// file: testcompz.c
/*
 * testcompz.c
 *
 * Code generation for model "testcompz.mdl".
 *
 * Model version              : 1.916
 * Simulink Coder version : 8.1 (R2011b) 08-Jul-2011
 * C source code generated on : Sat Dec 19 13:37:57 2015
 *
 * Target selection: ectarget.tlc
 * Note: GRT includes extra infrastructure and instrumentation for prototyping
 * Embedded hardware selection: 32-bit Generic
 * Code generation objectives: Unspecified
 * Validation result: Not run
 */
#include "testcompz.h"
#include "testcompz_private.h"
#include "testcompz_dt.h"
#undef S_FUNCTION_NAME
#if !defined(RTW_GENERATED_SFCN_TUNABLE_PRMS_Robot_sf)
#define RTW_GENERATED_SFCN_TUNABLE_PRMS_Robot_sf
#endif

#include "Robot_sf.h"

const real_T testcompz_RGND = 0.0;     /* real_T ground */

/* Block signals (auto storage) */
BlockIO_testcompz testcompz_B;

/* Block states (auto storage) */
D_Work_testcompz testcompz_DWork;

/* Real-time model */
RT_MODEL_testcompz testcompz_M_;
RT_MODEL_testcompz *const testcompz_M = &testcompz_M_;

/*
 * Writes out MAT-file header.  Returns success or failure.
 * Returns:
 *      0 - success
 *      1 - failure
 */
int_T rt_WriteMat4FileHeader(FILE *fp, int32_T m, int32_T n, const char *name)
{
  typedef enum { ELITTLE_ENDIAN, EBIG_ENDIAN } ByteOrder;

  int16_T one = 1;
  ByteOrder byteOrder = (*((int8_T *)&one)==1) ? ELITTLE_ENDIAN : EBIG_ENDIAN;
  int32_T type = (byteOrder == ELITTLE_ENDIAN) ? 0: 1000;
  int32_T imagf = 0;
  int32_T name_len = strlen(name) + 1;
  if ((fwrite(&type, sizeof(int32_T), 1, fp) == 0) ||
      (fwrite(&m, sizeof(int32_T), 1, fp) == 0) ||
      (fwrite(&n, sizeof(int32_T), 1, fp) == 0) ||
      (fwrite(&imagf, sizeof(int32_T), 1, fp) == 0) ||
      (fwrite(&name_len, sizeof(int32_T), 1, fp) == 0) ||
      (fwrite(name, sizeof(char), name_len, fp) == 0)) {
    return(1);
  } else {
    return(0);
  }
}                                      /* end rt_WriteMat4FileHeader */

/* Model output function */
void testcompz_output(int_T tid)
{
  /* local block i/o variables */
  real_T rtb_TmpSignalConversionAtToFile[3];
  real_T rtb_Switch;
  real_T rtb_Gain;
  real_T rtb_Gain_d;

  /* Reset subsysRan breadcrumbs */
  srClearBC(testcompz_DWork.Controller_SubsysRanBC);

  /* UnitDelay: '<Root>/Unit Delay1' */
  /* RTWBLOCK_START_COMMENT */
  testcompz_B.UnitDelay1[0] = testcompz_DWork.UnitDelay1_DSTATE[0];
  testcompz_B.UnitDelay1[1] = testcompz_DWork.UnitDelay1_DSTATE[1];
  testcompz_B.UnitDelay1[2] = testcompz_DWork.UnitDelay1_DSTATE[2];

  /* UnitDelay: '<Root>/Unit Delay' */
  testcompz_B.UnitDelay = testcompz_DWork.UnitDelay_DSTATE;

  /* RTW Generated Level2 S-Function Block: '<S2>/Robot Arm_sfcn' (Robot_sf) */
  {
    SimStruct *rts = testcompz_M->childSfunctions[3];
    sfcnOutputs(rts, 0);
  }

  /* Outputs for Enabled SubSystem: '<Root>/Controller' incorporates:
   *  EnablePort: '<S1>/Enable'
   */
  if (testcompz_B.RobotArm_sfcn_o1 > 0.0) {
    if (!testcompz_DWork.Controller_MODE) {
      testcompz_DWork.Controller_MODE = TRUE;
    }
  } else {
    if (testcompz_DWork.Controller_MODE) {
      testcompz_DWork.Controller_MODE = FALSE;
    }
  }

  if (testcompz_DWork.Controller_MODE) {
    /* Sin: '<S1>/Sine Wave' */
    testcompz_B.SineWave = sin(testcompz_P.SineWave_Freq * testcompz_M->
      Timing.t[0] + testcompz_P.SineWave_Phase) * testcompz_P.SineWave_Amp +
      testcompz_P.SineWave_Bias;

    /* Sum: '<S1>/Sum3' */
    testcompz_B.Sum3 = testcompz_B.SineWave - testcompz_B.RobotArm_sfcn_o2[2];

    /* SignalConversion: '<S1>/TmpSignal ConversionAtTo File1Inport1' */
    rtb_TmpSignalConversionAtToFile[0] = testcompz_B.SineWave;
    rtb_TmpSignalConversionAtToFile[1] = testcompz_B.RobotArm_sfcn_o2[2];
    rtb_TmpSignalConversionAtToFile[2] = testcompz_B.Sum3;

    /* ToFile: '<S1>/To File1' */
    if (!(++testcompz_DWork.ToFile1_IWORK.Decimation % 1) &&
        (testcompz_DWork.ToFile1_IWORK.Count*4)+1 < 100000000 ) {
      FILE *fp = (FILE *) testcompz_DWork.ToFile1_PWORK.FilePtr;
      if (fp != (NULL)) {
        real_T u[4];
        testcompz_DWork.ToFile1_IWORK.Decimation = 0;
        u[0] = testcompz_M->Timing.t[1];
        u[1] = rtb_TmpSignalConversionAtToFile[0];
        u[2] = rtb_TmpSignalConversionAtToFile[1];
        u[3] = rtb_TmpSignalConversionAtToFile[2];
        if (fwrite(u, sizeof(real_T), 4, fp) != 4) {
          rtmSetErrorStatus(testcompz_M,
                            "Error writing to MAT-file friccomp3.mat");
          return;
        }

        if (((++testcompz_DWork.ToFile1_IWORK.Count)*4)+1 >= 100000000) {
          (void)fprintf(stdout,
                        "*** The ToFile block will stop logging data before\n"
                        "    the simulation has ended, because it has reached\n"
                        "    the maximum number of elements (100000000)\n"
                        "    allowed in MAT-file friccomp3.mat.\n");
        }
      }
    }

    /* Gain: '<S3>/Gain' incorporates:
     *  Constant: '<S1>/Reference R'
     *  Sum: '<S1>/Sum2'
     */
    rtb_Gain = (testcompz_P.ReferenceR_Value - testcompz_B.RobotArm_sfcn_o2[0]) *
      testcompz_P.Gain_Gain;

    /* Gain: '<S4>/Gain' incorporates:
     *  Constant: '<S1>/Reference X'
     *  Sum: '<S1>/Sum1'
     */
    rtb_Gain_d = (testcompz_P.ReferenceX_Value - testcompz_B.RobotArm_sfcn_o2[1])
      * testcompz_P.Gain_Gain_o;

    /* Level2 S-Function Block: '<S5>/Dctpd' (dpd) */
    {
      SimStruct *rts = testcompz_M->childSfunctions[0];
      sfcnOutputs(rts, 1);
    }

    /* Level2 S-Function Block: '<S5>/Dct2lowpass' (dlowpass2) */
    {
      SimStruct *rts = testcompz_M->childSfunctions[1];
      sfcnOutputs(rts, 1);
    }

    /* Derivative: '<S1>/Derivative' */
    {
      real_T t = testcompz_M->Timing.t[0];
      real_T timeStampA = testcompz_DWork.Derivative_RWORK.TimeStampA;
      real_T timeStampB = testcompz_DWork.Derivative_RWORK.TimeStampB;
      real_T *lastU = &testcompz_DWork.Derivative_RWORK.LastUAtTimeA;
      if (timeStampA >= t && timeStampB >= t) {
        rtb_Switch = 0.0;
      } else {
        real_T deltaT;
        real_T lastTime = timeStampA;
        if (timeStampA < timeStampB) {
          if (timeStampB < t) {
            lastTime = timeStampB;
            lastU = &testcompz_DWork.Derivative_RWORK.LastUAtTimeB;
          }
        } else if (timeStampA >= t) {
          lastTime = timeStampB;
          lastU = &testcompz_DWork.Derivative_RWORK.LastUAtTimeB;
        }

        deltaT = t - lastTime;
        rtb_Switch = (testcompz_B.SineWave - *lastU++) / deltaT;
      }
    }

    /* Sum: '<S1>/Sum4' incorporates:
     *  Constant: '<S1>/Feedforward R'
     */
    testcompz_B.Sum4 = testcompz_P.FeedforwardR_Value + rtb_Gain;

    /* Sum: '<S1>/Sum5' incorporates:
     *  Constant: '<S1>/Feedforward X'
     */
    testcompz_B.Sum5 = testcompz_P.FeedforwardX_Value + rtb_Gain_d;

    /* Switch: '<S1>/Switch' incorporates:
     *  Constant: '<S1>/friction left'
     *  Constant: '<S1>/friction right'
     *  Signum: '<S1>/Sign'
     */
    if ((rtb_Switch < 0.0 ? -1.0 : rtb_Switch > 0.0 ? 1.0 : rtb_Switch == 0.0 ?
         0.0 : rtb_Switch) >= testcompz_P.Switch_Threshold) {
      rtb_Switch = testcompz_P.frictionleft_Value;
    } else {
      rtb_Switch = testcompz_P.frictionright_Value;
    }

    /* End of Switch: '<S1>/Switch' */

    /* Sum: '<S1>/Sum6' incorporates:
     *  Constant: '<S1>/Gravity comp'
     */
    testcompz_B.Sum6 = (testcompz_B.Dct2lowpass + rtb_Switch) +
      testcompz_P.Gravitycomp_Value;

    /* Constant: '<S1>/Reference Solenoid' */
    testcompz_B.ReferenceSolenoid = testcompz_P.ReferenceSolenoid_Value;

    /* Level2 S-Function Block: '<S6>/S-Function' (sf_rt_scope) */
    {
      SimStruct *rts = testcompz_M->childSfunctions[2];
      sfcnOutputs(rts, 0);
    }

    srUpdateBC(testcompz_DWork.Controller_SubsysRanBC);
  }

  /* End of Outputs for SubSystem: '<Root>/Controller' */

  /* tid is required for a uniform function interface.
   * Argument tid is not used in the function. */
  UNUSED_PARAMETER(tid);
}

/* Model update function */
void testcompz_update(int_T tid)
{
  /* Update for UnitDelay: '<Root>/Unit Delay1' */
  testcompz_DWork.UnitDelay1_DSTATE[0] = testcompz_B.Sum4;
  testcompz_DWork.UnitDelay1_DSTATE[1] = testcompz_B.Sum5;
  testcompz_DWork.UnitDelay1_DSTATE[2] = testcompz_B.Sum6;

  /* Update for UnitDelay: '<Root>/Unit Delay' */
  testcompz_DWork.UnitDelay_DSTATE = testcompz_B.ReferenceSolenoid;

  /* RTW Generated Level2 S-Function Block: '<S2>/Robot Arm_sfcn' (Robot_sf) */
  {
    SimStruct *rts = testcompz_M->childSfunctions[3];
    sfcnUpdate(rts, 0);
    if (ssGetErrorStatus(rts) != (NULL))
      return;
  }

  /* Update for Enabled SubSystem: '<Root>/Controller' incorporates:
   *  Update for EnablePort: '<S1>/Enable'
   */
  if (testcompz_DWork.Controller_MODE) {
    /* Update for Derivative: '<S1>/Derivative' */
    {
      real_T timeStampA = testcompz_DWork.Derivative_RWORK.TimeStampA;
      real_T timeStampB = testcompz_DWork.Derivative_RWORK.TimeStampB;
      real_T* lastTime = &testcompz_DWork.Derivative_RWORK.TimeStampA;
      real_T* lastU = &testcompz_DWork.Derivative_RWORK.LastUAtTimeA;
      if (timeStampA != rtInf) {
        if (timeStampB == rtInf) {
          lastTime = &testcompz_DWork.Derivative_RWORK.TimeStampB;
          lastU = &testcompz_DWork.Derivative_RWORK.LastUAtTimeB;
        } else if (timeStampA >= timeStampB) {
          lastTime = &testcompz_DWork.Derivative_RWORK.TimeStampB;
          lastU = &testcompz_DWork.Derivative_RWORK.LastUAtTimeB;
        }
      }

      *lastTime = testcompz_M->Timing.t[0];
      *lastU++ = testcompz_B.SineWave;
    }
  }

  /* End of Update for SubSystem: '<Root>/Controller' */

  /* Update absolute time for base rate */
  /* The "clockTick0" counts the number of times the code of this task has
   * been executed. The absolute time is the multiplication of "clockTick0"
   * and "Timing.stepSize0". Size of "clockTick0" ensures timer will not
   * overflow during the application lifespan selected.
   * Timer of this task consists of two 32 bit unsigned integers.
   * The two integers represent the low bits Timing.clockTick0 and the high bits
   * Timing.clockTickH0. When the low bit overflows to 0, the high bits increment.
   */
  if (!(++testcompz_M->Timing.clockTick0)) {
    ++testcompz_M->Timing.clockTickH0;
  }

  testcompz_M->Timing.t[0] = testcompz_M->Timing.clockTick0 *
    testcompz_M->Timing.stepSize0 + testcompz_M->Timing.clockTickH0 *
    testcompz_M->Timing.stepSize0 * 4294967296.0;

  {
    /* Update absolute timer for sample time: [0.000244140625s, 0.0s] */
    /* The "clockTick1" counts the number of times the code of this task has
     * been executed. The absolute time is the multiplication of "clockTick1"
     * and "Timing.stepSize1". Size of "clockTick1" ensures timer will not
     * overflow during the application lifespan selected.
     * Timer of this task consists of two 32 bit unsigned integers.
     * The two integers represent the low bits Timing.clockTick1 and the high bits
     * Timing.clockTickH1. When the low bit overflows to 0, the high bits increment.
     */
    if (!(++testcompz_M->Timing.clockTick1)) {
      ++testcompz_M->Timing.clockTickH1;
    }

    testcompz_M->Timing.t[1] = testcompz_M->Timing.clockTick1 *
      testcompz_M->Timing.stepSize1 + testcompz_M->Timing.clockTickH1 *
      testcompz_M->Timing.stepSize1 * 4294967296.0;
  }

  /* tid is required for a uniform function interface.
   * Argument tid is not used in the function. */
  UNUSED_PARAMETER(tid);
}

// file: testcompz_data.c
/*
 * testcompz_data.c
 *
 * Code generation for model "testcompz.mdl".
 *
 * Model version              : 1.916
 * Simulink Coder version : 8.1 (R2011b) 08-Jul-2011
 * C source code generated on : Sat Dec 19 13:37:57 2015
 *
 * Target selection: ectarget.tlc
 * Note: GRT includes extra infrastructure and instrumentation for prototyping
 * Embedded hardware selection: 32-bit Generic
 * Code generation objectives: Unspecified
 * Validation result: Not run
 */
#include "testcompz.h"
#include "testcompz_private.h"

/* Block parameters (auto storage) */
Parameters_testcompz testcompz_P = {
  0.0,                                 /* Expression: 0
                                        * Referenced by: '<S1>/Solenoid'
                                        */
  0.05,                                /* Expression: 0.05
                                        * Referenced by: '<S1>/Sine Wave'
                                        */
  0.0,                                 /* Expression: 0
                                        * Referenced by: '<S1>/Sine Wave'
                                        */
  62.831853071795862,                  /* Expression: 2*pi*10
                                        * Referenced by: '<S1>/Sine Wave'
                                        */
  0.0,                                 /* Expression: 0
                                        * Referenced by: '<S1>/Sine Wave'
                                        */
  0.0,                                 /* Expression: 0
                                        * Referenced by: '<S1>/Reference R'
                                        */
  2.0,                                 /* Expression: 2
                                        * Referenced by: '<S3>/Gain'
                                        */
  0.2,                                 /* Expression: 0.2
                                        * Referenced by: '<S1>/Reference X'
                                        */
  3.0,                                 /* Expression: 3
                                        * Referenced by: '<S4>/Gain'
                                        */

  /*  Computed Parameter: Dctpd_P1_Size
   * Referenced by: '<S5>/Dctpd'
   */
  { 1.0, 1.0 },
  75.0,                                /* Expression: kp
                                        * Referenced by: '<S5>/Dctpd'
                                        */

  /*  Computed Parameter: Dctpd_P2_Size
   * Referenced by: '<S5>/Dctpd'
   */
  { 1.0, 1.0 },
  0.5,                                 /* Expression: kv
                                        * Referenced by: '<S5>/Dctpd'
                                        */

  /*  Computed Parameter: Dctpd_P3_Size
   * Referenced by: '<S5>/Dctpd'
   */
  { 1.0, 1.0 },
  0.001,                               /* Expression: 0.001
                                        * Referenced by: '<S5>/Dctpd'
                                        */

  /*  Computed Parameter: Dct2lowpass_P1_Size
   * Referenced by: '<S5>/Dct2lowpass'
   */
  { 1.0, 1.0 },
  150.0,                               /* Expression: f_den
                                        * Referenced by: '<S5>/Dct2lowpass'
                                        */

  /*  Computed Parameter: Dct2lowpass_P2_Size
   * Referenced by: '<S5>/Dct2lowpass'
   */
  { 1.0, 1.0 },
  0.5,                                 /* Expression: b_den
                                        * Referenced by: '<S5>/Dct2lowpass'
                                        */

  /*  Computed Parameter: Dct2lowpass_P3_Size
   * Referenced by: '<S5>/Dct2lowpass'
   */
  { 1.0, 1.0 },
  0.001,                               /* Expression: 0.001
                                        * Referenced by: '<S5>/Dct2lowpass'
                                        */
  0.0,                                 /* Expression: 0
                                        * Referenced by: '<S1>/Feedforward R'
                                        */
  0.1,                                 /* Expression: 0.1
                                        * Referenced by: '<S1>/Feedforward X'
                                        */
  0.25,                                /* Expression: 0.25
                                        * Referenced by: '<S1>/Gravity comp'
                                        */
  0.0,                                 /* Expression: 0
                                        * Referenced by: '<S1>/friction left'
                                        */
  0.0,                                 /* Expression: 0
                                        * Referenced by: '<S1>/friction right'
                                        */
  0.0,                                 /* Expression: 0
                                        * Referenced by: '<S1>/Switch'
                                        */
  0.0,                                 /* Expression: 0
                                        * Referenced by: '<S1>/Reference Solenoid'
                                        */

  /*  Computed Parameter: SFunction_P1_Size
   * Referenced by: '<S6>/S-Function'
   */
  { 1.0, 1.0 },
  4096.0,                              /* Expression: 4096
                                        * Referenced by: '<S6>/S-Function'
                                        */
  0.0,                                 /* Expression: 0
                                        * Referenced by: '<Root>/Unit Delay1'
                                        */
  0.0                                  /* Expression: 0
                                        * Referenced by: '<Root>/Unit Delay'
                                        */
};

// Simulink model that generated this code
simulink model "testcompz"  (Simulink 7.8)
settings: Solver=ode1  StartTime=0.0  StopTime=100  FixedStep=1/(1024*4)  RelTol=1e-3

== system testcompz ==
  Accelerometer : Display
  Controller : Subsystem
  Robot Arm : Subsystem
  Unit Delay : UnitDelay  SampleTime=-1
  Unit Delay1 : UnitDelay  SampleTime=-1
  time1 : Display
  wires:
  Controller/1(Output) -> Unit Delay1/1
  Robot Arm/1(Homing Busy) -> Controller/Enable
  Robot Arm/2(Angle measurments [rad]) -> Controller/1(Angle Measurements [rad])
  Robot Arm/3(Airbag Status) -> time1/1
  Robot Arm/4(Accelerometer [V]) -> Accelerometer/1
  Controller/2(Solenoid) -> Unit Delay/1
  Unit Delay/1 -> Robot Arm/2(Solenoid)
  Unit Delay1/1 -> Robot Arm/1(Input [V])

== system testcompz/Controller ==
  Angle Measurements [rad] : Inport
  Enable : EnablePort
  Bus Creator1 : BusCreator  Inputs=3
  Controller R : Subsystem
  Controller X : Subsystem
  Controller Z : Subsystem
  Demux : Demux  Outputs=3
  Derivative : Derivative
  Feedforward R : Constant  Value=0
  Feedforward X : Constant  Value=0.1
  Gravity comp : Constant  Value=0.25
  Mux : Mux  Inputs=3
  RTScope : Subsystem
  Reference R : Constant  Value=0
  Reference Solenoid : Constant  Value=0
  Reference X : Constant  Value=0.2
  Reference Z : Constant  Value=0
  Sign : Signum
  Sine Wave : Sin  Amplitude=0.05  Frequency=2*pi*10  SampleTime=0
  Sum1 : Sum  Inputs=|+-
  Sum2 : Sum  Inputs=|+-
  Sum3 : Sum  Inputs=|+-
  Sum4 : Sum  Inputs=++|  SaturateOnIntegerOverflow=on  InputSameDT=on  OutDataTypeStr=Inherit: Same as first input
  Sum5 : Sum  Inputs=++|  SaturateOnIntegerOverflow=on  InputSameDT=on  OutDataTypeStr=Inherit: Same as first input
  Sum6 : Sum  Inputs=|+++  SaturateOnIntegerOverflow=on  InputSameDT=on  OutDataTypeStr=Inherit: Same as first input
  Switch : Switch
  To File1 : ToFile  Filename=friccomp3.mat  MatrixName=signals
  friction left : Constant  Value=0.2
  friction right : Constant  Value=-0.25
  time2 : Display
  Output : Outport
  Solenoid : Outport  Port=2  InitialOutput=0
  wires:
  Mux/1 -> Output/1
  Angle Measurements [rad]/1 -> Demux/1
  Sum2/1 -> Controller R/1(Input)
  Sum3/1 -> Controller Z/1(Input), Bus Creator1/3
  Sum1/1 -> Controller X/1(Input)
  Demux/1 -> Sum2/2  "R"
  Demux/2 -> Sum1/2  "X"
  Demux/3 -> time2/1, Sum3/2, Bus Creator1/2  "Z"
  Feedforward R/1 -> Sum4/1
  Controller R/1(Output) -> Sum4/2
  Sum4/1 -> Mux/1
  Controller X/1(Output) -> Sum5/2
  Sum5/1 -> Mux/2
  Sum6/1 -> Mux/3
  Reference R/1 -> Sum2/1
  Reference Solenoid/1 -> Solenoid/1
  Sine Wave/1 -> Derivative/1, Bus Creator1/1, Sum3/1
  Derivative/1 -> Sign/1
  Sign/1 -> Switch/2
  friction right/1 -> Switch/3
  friction left/1 -> Switch/1
  Bus Creator1/1 -> To File1/1
  Feedforward X/1 -> Sum5/1
  Reference X/1 -> Sum1/1
  Controller Z/1(Output) -> Sum6/1
  Gravity comp/1 -> Sum6/3
  Switch/1 -> Sum6/2

== system testcompz/Robot Arm ==
  Input [V] : Inport
  Solenoid : Inport  Port=2
  Robot Arm_sfcn : S-Function  FunctionName=Robot_sf  SFunctionModules=ec_Ebox dweakint dpd dnotch dlowpass2 ec_EboxResetEnc  EnableBusSupport=off  mask{rtw_sf_name=Robot_sf, showVar=off}
      mask prompts: rtw_sf_name "Generated S-function name (model_sf):"; showVar "Show module list"
      mask help: Simulink Coder generated S-function.
      mask init:
      | displist = '';
      | if ~strcmp(get_param(gcb, 'FunctionName'), rtw_sf_name);
      |   set_param(gcb, 'FunctionName', rtw_sf_name);
      | end
      | % Check if we are generating code
      | rtw_mode = false;
      | if strcmpi(get_param(bdroot(gcb),'SimulationStatus'),'Initializing')
      | 	rtw_mode = strcmpi(get_param(bdroot(gcb),'BuildingRTWCode'),'on') && ...
      | 		~strcmpi(get_param(bdroot(gcb),'TargetStyle'),'SimulationTarget');
      | end
      | if showVar || rtw_mode
      | 	if exist('rtwsfunc') == 2 | exist('rtwsfunc') == 6
      | 		tmplist = rtwsfunc(rtw_sf_name,gcb);
      | 		tmplist = ['\nList of Modules:\n', tmplist];
      | 	elseif showVar
      | 		tmplist = '\nList of Modules:\nNot licensed\n';
      |  	end
      | end
      | if showVar
      |   displist = tmplist;
      | end
  __InputSSForSFun__ : Subsystem
  __OutputSSForSFun__ : Subsystem
  Homing Busy : Outport
  Angle measurments [rad] : Outport  Port=2
  Airbag Status : Outport  Port=3
  Accelerometer [V] : Outport  Port=4
  wires:
  Input [V]/1 -> __InputSSForSFun__/1(Input [V])
  Solenoid/1 -> __InputSSForSFun__/2(Solenoid)
  __InputSSForSFun__/1(__UniqueOutportName__1__) -> Robot Arm_sfcn/1
  __InputSSForSFun__/2(__UniqueOutportName__2__) -> Robot Arm_sfcn/2
  Robot Arm_sfcn/1 -> __OutputSSForSFun__/1(__UniqueInportName__1__)
  Robot Arm_sfcn/2 -> __OutputSSForSFun__/2(__UniqueInportName__2__)
  Robot Arm_sfcn/3 -> __OutputSSForSFun__/3(__UniqueInportName__3__)
  Robot Arm_sfcn/4 -> __OutputSSForSFun__/4(__UniqueInportName__4__)
  __OutputSSForSFun__/1(Homing Busy) -> Homing Busy/1
  __OutputSSForSFun__/2(Angle measurments [rad]) -> Angle measurments [rad]/1
  __OutputSSForSFun__/3(Airbag Status) -> Airbag Status/1
  __OutputSSForSFun__/4(Accelerometer [V]) -> Accelerometer [V]/1

== system testcompz/Controller/Controller R ==
  Input : Inport
  Gain : Gain  Gain=2
  Output : Outport
  wires:
  Input/1 -> Gain/1
  Gain/1 -> Output/1

== system testcompz/Controller/Controller X ==
  Input : Inport
  Gain : Gain  Gain=3
  Output : Outport
  wires:
  Gain/1 -> Output/1
  Input/1 -> Gain/1

== system testcompz/Controller/Controller Z ==
  Input : Inport
  Dct2lowpass : S-Function  FunctionName=dlowpass2  Parameters=f_den, b_den, 0.001  EnableBusSupport=off  mask(dctools){f_den=150, b_den=0.5}
      mask prompts: f_den "Pole [Hz]"; b_den "Damping pole [-]"
      mask help: This block implements a discrete time 2nd order lowpass filter.
  Dctpd : S-Function  FunctionName=dpd  Parameters=kp, kv, 0.001  EnableBusSupport=off  mask(dctools){kp=75, kv=0.5}
      mask help: This block implements a discrete time pd filter.
  Output : Outport
  wires:
  Input/1 -> Dctpd/1
  Dctpd/1 -> Dct2lowpass/1
  Dct2lowpass/1 -> Output/1

== system testcompz/Controller/RTScope ==
  In1 : Inport
  In2 : Inport  Port=2
  In3 : Inport  Port=3
  In4 : Inport  Port=4
  In5 : Inport  Port=5
  In6 : Inport  Port=6
  In7 : Inport  Port=7
  In8 : Inport  Port=8
  Demux : Demux
  Mux : Mux  Inputs=8
  S-Function : S-Function  FunctionName=sf_rt_scope  Parameters=4096  EnableBusSupport=off
  Out1 : Outport
  Out2 : Outport  Port=2
  Out3 : Outport  Port=3
  Out4 : Outport  Port=4
  wires:
  In8/1 -> Mux/8
  In7/1 -> Mux/7
  In6/1 -> Mux/6
  In5/1 -> Mux/5
  In4/1 -> Mux/4
  In3/1 -> Mux/3
  In2/1 -> Mux/2
  In1/1 -> Mux/1
  Demux/4 -> Out4/1
  Demux/3 -> Out3/1
  Demux/2 -> Out2/1
  Demux/1 -> Out1/1
  S-Function/1 -> Demux/1
  Mux/1 -> S-Function/1

== system testcompz/Robot Arm/__InputSSForSFun__ ==
  Input [V] : Inport
  Solenoid : Inport  Port=2
  __UniqueOutportName__1__ : Outport
  __UniqueOutportName__2__ : Outport  Port=2
  wires:
  Input [V]/1 -> __UniqueOutportName__1__/1
  Solenoid/1 -> __UniqueOutportName__2__/1

== system testcompz/Robot Arm/__OutputSSForSFun__ ==
  __UniqueInportName__1__ : Inport
  __UniqueInportName__2__ : Inport  Port=2
  __UniqueInportName__3__ : Inport  Port=3
  __UniqueInportName__4__ : Inport  Port=4
  Homing Busy : Outport
  Angle measurments [rad] : Outport  Port=2
  Airbag Status : Outport  Port=3
  Accelerometer [V] : Outport  Port=4
  wires:
  __UniqueInportName__1__/1 -> Homing Busy/1
  __UniqueInportName__2__/1 -> Angle measurments [rad]/1
  __UniqueInportName__3__/1 -> Airbag Status/1
  __UniqueInportName__4__/1 -> Accelerometer [V]/1
